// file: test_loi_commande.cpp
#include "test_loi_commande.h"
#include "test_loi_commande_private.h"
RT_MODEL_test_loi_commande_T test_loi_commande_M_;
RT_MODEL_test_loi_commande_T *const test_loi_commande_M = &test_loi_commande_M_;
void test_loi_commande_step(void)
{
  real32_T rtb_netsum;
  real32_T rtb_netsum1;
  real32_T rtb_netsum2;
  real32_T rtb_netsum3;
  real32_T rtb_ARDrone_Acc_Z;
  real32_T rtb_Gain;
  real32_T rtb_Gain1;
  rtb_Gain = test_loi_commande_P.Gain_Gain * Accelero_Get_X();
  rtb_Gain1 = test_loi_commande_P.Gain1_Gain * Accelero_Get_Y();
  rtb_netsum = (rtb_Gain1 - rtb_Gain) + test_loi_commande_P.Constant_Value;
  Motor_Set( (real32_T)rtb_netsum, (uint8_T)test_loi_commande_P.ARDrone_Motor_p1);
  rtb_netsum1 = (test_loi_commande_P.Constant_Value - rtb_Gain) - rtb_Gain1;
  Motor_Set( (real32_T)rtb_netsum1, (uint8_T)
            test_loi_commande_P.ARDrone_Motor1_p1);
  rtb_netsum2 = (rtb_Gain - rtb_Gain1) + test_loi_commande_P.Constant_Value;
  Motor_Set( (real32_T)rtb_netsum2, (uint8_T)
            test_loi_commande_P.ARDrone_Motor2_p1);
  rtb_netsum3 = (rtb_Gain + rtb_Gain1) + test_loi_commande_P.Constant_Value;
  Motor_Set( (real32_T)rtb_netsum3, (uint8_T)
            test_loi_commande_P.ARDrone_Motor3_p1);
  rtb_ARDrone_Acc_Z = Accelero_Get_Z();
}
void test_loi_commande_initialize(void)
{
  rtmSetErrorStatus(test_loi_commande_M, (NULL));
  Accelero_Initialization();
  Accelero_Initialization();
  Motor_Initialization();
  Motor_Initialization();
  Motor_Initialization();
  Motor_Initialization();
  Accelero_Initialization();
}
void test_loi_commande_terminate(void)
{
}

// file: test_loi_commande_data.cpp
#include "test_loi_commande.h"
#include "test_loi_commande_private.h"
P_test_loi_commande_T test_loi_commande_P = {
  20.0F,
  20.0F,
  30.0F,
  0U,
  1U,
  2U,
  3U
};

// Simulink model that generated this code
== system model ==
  Motors#1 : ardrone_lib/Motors  <- 1: netsum, 2: netsum1, 3: netsum2, 4: netsum3
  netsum : Sum  Inputs=-++  <- 1: Gain, 2: Gain1, 3: Constant
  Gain : Gain  Gain=20  <- 1: Accelerometer#1
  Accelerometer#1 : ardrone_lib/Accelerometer
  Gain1 : Gain  Gain=20  <- 1: Accelerometer#1/2
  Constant : Constant  Value=30
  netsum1 : Sum  Inputs=--+  <- 1: Gain, 2: Gain1, 3: Constant
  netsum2 : Sum  Inputs=+-+  <- 1: Gain, 2: Gain1, 3: Constant
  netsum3 : Sum  Inputs=+++  <- 1: Gain, 2: Gain1, 3: Constant
